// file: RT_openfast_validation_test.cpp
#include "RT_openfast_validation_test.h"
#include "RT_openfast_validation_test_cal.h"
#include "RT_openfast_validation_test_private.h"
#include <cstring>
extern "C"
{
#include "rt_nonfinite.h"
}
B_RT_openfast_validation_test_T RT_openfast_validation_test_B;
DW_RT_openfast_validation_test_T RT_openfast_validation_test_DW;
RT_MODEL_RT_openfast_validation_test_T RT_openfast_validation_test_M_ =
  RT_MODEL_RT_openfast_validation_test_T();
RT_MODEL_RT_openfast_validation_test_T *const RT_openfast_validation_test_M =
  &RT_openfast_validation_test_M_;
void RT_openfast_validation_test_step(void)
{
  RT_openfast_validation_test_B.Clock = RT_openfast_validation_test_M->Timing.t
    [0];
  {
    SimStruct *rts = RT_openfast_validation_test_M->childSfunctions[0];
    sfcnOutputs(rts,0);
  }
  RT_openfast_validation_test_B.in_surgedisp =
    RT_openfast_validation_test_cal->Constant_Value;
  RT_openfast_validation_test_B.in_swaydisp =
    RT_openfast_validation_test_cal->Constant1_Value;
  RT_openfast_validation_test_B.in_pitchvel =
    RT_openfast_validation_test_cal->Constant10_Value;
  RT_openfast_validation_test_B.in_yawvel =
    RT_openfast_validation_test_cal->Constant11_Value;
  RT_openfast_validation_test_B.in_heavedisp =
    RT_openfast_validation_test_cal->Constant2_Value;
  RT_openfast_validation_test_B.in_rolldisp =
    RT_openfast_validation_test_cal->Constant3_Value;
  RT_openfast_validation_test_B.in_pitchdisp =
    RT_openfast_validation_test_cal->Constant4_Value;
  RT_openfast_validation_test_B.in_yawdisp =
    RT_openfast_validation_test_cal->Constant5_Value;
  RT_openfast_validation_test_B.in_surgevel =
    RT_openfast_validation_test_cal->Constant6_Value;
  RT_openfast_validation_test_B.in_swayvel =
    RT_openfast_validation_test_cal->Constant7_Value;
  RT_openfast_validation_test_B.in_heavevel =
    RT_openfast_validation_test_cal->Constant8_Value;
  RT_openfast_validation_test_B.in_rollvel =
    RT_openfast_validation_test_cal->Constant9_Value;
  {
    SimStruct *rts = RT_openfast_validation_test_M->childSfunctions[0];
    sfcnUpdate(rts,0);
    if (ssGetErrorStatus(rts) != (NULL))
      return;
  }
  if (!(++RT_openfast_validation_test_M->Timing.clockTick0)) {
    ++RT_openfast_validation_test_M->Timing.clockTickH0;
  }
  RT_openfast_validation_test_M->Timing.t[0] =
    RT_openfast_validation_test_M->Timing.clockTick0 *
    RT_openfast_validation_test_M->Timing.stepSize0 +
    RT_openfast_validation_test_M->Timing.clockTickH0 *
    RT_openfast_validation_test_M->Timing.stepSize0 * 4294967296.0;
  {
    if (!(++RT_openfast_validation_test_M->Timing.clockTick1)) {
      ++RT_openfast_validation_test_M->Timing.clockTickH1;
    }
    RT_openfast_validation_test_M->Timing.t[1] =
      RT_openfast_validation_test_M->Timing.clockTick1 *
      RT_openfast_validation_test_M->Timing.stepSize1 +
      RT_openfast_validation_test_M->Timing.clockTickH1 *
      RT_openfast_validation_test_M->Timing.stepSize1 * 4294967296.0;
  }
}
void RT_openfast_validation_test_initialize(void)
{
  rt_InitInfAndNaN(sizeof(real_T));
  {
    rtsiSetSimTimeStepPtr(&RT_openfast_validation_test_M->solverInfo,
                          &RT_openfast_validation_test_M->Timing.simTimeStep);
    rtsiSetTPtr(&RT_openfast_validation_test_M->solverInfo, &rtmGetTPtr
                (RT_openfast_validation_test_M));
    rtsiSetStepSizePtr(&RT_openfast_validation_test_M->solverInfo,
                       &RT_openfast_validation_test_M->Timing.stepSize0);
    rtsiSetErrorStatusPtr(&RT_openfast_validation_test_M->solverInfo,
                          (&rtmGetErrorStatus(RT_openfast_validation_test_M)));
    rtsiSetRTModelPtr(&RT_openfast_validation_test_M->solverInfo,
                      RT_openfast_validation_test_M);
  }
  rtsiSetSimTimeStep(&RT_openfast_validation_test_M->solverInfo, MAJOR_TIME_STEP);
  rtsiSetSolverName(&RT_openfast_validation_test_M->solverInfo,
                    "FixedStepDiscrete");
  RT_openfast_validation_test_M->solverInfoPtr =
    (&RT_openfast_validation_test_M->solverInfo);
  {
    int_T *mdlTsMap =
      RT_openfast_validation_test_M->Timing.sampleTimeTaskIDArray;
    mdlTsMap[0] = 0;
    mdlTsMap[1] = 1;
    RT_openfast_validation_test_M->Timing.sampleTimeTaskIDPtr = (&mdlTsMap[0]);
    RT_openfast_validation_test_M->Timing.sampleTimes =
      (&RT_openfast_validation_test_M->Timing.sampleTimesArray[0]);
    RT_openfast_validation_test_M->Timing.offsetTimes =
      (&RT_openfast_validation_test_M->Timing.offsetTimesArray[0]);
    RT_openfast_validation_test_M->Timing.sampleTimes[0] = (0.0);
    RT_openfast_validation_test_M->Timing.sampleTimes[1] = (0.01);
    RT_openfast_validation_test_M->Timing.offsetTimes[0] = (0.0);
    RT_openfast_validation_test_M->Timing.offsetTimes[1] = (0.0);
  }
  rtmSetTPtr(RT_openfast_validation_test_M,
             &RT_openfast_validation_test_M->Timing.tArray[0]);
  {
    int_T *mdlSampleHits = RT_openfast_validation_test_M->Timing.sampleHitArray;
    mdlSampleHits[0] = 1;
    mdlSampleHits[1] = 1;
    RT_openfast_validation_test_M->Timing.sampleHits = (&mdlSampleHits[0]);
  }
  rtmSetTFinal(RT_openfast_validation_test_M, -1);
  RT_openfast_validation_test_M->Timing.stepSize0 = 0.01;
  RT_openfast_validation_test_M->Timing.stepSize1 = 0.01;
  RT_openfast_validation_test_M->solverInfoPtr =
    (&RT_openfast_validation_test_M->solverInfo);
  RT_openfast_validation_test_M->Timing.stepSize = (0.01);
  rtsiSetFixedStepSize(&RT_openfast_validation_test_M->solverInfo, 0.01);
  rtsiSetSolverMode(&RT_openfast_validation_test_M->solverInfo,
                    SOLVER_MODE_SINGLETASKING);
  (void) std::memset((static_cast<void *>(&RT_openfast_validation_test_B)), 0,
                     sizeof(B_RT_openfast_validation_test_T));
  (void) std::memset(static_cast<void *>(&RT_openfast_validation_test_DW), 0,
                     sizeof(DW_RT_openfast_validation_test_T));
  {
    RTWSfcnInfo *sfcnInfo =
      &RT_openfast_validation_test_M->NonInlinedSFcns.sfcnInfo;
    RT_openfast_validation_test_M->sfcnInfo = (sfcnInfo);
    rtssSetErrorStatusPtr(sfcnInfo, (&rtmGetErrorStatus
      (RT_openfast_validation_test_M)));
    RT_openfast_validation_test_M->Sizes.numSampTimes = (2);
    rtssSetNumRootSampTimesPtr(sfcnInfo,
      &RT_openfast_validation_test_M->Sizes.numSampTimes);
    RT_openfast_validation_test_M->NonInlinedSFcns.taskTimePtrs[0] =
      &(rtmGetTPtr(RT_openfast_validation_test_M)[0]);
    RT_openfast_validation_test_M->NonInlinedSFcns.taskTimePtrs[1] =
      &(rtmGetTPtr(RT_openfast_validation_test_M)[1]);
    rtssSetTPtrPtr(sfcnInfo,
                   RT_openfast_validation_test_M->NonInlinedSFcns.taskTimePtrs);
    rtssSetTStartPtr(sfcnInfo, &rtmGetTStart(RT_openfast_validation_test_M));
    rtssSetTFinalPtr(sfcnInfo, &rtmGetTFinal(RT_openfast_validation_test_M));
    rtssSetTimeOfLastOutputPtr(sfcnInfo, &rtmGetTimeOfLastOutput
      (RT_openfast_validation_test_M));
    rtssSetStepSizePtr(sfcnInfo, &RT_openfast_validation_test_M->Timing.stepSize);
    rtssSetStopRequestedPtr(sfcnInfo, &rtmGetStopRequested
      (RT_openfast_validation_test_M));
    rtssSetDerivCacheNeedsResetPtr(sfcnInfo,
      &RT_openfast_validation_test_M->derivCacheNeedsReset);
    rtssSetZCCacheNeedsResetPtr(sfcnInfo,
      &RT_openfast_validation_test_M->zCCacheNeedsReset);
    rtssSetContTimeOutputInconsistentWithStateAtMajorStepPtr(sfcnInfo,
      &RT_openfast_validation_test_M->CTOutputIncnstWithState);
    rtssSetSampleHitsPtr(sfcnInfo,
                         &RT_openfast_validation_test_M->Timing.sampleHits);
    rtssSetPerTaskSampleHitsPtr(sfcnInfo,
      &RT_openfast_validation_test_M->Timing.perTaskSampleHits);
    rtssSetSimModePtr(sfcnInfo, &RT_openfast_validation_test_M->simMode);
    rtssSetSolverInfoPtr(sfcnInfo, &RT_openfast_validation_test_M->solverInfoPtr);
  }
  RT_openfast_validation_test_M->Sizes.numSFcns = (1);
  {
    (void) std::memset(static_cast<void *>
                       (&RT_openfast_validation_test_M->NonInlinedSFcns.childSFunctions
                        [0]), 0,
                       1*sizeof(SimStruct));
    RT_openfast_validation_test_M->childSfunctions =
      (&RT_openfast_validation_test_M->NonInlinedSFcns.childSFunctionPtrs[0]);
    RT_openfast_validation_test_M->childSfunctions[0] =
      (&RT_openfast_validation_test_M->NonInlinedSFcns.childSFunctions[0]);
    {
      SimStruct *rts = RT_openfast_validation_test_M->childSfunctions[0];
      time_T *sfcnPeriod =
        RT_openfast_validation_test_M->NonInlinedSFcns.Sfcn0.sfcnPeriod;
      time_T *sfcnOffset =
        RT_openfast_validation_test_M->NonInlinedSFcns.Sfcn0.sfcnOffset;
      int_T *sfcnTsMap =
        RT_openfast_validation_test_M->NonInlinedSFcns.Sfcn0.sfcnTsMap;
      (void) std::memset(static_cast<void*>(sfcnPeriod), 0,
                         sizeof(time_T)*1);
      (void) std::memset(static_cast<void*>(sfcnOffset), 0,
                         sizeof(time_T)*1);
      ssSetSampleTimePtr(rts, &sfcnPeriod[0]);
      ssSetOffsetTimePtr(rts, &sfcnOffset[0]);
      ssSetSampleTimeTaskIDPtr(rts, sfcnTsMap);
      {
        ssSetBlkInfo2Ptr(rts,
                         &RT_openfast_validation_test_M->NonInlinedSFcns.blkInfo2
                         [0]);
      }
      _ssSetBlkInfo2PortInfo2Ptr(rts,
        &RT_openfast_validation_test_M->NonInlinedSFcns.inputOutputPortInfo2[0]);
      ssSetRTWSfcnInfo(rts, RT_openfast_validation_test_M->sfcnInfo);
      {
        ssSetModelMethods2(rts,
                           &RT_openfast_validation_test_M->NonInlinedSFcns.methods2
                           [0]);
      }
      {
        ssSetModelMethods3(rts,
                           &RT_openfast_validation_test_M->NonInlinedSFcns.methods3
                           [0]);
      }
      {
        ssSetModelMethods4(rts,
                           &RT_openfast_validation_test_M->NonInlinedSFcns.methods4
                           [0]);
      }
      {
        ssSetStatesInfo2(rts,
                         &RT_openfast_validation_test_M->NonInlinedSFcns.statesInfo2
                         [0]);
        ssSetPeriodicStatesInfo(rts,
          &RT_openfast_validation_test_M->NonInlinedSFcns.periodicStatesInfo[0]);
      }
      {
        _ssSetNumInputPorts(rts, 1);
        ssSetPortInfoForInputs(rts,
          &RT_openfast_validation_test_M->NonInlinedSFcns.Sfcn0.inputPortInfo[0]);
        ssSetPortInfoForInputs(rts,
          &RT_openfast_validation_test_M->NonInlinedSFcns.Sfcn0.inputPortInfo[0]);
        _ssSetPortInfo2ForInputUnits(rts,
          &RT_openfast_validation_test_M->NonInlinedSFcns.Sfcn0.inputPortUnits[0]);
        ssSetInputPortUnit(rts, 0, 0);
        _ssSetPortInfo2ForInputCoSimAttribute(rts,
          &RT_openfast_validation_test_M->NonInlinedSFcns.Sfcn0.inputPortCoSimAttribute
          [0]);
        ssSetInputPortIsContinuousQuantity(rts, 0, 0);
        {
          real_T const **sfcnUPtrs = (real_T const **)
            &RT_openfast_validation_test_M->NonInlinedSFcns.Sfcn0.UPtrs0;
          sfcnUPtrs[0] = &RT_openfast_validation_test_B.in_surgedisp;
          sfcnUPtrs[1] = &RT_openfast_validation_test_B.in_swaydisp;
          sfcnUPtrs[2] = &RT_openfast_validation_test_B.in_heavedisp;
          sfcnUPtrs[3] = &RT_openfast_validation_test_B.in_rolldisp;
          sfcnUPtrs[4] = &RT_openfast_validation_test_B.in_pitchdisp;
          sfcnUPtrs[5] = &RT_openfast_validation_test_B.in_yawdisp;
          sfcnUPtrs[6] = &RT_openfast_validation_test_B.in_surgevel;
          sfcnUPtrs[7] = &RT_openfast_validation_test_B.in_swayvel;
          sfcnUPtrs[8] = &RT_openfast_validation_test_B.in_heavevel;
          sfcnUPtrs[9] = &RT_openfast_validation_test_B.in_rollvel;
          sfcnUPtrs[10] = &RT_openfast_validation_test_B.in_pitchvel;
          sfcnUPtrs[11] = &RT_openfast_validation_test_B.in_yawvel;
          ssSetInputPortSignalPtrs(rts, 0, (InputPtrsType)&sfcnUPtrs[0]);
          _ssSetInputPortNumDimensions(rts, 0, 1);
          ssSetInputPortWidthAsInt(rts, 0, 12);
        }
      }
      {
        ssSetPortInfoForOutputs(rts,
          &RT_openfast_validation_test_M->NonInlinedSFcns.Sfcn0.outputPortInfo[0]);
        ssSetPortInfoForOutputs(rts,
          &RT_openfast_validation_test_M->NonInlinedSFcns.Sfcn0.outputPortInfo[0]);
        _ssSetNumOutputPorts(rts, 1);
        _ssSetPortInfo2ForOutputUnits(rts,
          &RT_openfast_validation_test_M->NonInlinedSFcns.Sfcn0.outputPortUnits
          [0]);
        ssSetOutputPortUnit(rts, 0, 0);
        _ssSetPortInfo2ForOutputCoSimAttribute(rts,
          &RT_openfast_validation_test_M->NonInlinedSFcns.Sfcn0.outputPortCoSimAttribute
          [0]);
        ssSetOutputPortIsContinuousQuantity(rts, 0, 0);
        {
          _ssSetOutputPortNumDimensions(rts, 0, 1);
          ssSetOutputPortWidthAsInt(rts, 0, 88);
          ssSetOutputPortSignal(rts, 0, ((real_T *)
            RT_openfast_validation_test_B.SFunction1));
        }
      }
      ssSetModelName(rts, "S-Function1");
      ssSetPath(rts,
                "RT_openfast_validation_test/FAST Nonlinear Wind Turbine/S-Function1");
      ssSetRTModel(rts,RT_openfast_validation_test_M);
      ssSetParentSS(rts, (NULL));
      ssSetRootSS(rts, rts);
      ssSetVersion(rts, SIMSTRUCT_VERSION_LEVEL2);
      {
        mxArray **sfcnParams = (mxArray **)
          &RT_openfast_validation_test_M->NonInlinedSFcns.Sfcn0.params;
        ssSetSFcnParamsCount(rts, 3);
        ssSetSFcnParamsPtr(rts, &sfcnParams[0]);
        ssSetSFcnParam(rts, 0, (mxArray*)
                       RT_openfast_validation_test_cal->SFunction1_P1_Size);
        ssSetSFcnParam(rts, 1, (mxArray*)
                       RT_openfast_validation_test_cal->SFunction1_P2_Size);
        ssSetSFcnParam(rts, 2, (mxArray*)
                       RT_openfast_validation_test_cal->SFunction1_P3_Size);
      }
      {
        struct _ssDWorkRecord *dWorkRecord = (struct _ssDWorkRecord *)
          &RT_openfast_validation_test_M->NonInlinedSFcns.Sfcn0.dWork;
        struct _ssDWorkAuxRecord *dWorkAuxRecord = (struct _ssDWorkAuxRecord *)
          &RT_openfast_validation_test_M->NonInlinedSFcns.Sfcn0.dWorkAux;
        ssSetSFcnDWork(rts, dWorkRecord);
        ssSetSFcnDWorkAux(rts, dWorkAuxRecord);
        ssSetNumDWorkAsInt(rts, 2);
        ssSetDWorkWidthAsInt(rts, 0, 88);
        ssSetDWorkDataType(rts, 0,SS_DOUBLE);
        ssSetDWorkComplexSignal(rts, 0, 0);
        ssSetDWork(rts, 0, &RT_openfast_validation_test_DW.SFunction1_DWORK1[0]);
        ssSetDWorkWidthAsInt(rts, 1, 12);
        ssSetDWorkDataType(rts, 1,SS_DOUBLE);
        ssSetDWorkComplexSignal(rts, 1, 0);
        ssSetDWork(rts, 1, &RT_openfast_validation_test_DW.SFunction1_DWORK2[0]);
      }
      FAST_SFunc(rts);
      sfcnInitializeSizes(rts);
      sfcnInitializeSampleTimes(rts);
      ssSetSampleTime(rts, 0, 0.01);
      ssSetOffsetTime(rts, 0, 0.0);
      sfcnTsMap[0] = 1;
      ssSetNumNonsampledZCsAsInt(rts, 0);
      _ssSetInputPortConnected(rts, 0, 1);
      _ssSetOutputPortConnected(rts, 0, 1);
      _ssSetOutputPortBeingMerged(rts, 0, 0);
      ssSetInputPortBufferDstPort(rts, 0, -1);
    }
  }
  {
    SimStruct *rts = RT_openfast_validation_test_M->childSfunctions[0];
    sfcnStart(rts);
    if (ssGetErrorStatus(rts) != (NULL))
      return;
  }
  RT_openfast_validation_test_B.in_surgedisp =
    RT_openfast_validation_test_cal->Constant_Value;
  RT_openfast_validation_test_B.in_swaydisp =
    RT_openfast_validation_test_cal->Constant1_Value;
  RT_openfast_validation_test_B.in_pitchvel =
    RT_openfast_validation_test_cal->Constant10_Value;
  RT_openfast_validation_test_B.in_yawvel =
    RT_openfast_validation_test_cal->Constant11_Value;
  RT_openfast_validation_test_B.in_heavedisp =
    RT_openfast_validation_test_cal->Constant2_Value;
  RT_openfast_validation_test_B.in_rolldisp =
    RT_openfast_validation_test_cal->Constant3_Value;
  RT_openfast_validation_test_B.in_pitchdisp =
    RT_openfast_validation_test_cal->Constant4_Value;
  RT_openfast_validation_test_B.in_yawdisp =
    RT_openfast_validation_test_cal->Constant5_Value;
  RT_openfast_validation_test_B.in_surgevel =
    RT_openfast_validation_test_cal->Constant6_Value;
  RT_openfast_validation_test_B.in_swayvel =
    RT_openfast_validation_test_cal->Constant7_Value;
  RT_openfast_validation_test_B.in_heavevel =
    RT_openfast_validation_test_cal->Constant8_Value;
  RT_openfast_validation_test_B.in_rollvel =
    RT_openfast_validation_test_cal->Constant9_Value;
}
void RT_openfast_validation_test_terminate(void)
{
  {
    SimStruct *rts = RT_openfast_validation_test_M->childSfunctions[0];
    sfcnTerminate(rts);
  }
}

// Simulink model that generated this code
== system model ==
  Clock : Clock
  SFunction1 : S-Function  FunctionName=FAST_SFunc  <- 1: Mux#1
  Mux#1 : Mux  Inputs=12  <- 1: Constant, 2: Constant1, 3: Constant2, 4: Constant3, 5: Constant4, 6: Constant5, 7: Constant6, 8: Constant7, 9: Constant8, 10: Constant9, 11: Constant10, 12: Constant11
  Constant : Constant  Value=0
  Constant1 : Constant  Value=0
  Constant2 : Constant  Value=0
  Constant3 : Constant  Value=0
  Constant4 : Constant  Value=0
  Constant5 : Constant  Value=0
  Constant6 : Constant  Value=0
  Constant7 : Constant  Value=0
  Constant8 : Constant  Value=0
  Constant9 : Constant  Value=0
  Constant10 : Constant  Value=0
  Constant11 : Constant  Value=0
